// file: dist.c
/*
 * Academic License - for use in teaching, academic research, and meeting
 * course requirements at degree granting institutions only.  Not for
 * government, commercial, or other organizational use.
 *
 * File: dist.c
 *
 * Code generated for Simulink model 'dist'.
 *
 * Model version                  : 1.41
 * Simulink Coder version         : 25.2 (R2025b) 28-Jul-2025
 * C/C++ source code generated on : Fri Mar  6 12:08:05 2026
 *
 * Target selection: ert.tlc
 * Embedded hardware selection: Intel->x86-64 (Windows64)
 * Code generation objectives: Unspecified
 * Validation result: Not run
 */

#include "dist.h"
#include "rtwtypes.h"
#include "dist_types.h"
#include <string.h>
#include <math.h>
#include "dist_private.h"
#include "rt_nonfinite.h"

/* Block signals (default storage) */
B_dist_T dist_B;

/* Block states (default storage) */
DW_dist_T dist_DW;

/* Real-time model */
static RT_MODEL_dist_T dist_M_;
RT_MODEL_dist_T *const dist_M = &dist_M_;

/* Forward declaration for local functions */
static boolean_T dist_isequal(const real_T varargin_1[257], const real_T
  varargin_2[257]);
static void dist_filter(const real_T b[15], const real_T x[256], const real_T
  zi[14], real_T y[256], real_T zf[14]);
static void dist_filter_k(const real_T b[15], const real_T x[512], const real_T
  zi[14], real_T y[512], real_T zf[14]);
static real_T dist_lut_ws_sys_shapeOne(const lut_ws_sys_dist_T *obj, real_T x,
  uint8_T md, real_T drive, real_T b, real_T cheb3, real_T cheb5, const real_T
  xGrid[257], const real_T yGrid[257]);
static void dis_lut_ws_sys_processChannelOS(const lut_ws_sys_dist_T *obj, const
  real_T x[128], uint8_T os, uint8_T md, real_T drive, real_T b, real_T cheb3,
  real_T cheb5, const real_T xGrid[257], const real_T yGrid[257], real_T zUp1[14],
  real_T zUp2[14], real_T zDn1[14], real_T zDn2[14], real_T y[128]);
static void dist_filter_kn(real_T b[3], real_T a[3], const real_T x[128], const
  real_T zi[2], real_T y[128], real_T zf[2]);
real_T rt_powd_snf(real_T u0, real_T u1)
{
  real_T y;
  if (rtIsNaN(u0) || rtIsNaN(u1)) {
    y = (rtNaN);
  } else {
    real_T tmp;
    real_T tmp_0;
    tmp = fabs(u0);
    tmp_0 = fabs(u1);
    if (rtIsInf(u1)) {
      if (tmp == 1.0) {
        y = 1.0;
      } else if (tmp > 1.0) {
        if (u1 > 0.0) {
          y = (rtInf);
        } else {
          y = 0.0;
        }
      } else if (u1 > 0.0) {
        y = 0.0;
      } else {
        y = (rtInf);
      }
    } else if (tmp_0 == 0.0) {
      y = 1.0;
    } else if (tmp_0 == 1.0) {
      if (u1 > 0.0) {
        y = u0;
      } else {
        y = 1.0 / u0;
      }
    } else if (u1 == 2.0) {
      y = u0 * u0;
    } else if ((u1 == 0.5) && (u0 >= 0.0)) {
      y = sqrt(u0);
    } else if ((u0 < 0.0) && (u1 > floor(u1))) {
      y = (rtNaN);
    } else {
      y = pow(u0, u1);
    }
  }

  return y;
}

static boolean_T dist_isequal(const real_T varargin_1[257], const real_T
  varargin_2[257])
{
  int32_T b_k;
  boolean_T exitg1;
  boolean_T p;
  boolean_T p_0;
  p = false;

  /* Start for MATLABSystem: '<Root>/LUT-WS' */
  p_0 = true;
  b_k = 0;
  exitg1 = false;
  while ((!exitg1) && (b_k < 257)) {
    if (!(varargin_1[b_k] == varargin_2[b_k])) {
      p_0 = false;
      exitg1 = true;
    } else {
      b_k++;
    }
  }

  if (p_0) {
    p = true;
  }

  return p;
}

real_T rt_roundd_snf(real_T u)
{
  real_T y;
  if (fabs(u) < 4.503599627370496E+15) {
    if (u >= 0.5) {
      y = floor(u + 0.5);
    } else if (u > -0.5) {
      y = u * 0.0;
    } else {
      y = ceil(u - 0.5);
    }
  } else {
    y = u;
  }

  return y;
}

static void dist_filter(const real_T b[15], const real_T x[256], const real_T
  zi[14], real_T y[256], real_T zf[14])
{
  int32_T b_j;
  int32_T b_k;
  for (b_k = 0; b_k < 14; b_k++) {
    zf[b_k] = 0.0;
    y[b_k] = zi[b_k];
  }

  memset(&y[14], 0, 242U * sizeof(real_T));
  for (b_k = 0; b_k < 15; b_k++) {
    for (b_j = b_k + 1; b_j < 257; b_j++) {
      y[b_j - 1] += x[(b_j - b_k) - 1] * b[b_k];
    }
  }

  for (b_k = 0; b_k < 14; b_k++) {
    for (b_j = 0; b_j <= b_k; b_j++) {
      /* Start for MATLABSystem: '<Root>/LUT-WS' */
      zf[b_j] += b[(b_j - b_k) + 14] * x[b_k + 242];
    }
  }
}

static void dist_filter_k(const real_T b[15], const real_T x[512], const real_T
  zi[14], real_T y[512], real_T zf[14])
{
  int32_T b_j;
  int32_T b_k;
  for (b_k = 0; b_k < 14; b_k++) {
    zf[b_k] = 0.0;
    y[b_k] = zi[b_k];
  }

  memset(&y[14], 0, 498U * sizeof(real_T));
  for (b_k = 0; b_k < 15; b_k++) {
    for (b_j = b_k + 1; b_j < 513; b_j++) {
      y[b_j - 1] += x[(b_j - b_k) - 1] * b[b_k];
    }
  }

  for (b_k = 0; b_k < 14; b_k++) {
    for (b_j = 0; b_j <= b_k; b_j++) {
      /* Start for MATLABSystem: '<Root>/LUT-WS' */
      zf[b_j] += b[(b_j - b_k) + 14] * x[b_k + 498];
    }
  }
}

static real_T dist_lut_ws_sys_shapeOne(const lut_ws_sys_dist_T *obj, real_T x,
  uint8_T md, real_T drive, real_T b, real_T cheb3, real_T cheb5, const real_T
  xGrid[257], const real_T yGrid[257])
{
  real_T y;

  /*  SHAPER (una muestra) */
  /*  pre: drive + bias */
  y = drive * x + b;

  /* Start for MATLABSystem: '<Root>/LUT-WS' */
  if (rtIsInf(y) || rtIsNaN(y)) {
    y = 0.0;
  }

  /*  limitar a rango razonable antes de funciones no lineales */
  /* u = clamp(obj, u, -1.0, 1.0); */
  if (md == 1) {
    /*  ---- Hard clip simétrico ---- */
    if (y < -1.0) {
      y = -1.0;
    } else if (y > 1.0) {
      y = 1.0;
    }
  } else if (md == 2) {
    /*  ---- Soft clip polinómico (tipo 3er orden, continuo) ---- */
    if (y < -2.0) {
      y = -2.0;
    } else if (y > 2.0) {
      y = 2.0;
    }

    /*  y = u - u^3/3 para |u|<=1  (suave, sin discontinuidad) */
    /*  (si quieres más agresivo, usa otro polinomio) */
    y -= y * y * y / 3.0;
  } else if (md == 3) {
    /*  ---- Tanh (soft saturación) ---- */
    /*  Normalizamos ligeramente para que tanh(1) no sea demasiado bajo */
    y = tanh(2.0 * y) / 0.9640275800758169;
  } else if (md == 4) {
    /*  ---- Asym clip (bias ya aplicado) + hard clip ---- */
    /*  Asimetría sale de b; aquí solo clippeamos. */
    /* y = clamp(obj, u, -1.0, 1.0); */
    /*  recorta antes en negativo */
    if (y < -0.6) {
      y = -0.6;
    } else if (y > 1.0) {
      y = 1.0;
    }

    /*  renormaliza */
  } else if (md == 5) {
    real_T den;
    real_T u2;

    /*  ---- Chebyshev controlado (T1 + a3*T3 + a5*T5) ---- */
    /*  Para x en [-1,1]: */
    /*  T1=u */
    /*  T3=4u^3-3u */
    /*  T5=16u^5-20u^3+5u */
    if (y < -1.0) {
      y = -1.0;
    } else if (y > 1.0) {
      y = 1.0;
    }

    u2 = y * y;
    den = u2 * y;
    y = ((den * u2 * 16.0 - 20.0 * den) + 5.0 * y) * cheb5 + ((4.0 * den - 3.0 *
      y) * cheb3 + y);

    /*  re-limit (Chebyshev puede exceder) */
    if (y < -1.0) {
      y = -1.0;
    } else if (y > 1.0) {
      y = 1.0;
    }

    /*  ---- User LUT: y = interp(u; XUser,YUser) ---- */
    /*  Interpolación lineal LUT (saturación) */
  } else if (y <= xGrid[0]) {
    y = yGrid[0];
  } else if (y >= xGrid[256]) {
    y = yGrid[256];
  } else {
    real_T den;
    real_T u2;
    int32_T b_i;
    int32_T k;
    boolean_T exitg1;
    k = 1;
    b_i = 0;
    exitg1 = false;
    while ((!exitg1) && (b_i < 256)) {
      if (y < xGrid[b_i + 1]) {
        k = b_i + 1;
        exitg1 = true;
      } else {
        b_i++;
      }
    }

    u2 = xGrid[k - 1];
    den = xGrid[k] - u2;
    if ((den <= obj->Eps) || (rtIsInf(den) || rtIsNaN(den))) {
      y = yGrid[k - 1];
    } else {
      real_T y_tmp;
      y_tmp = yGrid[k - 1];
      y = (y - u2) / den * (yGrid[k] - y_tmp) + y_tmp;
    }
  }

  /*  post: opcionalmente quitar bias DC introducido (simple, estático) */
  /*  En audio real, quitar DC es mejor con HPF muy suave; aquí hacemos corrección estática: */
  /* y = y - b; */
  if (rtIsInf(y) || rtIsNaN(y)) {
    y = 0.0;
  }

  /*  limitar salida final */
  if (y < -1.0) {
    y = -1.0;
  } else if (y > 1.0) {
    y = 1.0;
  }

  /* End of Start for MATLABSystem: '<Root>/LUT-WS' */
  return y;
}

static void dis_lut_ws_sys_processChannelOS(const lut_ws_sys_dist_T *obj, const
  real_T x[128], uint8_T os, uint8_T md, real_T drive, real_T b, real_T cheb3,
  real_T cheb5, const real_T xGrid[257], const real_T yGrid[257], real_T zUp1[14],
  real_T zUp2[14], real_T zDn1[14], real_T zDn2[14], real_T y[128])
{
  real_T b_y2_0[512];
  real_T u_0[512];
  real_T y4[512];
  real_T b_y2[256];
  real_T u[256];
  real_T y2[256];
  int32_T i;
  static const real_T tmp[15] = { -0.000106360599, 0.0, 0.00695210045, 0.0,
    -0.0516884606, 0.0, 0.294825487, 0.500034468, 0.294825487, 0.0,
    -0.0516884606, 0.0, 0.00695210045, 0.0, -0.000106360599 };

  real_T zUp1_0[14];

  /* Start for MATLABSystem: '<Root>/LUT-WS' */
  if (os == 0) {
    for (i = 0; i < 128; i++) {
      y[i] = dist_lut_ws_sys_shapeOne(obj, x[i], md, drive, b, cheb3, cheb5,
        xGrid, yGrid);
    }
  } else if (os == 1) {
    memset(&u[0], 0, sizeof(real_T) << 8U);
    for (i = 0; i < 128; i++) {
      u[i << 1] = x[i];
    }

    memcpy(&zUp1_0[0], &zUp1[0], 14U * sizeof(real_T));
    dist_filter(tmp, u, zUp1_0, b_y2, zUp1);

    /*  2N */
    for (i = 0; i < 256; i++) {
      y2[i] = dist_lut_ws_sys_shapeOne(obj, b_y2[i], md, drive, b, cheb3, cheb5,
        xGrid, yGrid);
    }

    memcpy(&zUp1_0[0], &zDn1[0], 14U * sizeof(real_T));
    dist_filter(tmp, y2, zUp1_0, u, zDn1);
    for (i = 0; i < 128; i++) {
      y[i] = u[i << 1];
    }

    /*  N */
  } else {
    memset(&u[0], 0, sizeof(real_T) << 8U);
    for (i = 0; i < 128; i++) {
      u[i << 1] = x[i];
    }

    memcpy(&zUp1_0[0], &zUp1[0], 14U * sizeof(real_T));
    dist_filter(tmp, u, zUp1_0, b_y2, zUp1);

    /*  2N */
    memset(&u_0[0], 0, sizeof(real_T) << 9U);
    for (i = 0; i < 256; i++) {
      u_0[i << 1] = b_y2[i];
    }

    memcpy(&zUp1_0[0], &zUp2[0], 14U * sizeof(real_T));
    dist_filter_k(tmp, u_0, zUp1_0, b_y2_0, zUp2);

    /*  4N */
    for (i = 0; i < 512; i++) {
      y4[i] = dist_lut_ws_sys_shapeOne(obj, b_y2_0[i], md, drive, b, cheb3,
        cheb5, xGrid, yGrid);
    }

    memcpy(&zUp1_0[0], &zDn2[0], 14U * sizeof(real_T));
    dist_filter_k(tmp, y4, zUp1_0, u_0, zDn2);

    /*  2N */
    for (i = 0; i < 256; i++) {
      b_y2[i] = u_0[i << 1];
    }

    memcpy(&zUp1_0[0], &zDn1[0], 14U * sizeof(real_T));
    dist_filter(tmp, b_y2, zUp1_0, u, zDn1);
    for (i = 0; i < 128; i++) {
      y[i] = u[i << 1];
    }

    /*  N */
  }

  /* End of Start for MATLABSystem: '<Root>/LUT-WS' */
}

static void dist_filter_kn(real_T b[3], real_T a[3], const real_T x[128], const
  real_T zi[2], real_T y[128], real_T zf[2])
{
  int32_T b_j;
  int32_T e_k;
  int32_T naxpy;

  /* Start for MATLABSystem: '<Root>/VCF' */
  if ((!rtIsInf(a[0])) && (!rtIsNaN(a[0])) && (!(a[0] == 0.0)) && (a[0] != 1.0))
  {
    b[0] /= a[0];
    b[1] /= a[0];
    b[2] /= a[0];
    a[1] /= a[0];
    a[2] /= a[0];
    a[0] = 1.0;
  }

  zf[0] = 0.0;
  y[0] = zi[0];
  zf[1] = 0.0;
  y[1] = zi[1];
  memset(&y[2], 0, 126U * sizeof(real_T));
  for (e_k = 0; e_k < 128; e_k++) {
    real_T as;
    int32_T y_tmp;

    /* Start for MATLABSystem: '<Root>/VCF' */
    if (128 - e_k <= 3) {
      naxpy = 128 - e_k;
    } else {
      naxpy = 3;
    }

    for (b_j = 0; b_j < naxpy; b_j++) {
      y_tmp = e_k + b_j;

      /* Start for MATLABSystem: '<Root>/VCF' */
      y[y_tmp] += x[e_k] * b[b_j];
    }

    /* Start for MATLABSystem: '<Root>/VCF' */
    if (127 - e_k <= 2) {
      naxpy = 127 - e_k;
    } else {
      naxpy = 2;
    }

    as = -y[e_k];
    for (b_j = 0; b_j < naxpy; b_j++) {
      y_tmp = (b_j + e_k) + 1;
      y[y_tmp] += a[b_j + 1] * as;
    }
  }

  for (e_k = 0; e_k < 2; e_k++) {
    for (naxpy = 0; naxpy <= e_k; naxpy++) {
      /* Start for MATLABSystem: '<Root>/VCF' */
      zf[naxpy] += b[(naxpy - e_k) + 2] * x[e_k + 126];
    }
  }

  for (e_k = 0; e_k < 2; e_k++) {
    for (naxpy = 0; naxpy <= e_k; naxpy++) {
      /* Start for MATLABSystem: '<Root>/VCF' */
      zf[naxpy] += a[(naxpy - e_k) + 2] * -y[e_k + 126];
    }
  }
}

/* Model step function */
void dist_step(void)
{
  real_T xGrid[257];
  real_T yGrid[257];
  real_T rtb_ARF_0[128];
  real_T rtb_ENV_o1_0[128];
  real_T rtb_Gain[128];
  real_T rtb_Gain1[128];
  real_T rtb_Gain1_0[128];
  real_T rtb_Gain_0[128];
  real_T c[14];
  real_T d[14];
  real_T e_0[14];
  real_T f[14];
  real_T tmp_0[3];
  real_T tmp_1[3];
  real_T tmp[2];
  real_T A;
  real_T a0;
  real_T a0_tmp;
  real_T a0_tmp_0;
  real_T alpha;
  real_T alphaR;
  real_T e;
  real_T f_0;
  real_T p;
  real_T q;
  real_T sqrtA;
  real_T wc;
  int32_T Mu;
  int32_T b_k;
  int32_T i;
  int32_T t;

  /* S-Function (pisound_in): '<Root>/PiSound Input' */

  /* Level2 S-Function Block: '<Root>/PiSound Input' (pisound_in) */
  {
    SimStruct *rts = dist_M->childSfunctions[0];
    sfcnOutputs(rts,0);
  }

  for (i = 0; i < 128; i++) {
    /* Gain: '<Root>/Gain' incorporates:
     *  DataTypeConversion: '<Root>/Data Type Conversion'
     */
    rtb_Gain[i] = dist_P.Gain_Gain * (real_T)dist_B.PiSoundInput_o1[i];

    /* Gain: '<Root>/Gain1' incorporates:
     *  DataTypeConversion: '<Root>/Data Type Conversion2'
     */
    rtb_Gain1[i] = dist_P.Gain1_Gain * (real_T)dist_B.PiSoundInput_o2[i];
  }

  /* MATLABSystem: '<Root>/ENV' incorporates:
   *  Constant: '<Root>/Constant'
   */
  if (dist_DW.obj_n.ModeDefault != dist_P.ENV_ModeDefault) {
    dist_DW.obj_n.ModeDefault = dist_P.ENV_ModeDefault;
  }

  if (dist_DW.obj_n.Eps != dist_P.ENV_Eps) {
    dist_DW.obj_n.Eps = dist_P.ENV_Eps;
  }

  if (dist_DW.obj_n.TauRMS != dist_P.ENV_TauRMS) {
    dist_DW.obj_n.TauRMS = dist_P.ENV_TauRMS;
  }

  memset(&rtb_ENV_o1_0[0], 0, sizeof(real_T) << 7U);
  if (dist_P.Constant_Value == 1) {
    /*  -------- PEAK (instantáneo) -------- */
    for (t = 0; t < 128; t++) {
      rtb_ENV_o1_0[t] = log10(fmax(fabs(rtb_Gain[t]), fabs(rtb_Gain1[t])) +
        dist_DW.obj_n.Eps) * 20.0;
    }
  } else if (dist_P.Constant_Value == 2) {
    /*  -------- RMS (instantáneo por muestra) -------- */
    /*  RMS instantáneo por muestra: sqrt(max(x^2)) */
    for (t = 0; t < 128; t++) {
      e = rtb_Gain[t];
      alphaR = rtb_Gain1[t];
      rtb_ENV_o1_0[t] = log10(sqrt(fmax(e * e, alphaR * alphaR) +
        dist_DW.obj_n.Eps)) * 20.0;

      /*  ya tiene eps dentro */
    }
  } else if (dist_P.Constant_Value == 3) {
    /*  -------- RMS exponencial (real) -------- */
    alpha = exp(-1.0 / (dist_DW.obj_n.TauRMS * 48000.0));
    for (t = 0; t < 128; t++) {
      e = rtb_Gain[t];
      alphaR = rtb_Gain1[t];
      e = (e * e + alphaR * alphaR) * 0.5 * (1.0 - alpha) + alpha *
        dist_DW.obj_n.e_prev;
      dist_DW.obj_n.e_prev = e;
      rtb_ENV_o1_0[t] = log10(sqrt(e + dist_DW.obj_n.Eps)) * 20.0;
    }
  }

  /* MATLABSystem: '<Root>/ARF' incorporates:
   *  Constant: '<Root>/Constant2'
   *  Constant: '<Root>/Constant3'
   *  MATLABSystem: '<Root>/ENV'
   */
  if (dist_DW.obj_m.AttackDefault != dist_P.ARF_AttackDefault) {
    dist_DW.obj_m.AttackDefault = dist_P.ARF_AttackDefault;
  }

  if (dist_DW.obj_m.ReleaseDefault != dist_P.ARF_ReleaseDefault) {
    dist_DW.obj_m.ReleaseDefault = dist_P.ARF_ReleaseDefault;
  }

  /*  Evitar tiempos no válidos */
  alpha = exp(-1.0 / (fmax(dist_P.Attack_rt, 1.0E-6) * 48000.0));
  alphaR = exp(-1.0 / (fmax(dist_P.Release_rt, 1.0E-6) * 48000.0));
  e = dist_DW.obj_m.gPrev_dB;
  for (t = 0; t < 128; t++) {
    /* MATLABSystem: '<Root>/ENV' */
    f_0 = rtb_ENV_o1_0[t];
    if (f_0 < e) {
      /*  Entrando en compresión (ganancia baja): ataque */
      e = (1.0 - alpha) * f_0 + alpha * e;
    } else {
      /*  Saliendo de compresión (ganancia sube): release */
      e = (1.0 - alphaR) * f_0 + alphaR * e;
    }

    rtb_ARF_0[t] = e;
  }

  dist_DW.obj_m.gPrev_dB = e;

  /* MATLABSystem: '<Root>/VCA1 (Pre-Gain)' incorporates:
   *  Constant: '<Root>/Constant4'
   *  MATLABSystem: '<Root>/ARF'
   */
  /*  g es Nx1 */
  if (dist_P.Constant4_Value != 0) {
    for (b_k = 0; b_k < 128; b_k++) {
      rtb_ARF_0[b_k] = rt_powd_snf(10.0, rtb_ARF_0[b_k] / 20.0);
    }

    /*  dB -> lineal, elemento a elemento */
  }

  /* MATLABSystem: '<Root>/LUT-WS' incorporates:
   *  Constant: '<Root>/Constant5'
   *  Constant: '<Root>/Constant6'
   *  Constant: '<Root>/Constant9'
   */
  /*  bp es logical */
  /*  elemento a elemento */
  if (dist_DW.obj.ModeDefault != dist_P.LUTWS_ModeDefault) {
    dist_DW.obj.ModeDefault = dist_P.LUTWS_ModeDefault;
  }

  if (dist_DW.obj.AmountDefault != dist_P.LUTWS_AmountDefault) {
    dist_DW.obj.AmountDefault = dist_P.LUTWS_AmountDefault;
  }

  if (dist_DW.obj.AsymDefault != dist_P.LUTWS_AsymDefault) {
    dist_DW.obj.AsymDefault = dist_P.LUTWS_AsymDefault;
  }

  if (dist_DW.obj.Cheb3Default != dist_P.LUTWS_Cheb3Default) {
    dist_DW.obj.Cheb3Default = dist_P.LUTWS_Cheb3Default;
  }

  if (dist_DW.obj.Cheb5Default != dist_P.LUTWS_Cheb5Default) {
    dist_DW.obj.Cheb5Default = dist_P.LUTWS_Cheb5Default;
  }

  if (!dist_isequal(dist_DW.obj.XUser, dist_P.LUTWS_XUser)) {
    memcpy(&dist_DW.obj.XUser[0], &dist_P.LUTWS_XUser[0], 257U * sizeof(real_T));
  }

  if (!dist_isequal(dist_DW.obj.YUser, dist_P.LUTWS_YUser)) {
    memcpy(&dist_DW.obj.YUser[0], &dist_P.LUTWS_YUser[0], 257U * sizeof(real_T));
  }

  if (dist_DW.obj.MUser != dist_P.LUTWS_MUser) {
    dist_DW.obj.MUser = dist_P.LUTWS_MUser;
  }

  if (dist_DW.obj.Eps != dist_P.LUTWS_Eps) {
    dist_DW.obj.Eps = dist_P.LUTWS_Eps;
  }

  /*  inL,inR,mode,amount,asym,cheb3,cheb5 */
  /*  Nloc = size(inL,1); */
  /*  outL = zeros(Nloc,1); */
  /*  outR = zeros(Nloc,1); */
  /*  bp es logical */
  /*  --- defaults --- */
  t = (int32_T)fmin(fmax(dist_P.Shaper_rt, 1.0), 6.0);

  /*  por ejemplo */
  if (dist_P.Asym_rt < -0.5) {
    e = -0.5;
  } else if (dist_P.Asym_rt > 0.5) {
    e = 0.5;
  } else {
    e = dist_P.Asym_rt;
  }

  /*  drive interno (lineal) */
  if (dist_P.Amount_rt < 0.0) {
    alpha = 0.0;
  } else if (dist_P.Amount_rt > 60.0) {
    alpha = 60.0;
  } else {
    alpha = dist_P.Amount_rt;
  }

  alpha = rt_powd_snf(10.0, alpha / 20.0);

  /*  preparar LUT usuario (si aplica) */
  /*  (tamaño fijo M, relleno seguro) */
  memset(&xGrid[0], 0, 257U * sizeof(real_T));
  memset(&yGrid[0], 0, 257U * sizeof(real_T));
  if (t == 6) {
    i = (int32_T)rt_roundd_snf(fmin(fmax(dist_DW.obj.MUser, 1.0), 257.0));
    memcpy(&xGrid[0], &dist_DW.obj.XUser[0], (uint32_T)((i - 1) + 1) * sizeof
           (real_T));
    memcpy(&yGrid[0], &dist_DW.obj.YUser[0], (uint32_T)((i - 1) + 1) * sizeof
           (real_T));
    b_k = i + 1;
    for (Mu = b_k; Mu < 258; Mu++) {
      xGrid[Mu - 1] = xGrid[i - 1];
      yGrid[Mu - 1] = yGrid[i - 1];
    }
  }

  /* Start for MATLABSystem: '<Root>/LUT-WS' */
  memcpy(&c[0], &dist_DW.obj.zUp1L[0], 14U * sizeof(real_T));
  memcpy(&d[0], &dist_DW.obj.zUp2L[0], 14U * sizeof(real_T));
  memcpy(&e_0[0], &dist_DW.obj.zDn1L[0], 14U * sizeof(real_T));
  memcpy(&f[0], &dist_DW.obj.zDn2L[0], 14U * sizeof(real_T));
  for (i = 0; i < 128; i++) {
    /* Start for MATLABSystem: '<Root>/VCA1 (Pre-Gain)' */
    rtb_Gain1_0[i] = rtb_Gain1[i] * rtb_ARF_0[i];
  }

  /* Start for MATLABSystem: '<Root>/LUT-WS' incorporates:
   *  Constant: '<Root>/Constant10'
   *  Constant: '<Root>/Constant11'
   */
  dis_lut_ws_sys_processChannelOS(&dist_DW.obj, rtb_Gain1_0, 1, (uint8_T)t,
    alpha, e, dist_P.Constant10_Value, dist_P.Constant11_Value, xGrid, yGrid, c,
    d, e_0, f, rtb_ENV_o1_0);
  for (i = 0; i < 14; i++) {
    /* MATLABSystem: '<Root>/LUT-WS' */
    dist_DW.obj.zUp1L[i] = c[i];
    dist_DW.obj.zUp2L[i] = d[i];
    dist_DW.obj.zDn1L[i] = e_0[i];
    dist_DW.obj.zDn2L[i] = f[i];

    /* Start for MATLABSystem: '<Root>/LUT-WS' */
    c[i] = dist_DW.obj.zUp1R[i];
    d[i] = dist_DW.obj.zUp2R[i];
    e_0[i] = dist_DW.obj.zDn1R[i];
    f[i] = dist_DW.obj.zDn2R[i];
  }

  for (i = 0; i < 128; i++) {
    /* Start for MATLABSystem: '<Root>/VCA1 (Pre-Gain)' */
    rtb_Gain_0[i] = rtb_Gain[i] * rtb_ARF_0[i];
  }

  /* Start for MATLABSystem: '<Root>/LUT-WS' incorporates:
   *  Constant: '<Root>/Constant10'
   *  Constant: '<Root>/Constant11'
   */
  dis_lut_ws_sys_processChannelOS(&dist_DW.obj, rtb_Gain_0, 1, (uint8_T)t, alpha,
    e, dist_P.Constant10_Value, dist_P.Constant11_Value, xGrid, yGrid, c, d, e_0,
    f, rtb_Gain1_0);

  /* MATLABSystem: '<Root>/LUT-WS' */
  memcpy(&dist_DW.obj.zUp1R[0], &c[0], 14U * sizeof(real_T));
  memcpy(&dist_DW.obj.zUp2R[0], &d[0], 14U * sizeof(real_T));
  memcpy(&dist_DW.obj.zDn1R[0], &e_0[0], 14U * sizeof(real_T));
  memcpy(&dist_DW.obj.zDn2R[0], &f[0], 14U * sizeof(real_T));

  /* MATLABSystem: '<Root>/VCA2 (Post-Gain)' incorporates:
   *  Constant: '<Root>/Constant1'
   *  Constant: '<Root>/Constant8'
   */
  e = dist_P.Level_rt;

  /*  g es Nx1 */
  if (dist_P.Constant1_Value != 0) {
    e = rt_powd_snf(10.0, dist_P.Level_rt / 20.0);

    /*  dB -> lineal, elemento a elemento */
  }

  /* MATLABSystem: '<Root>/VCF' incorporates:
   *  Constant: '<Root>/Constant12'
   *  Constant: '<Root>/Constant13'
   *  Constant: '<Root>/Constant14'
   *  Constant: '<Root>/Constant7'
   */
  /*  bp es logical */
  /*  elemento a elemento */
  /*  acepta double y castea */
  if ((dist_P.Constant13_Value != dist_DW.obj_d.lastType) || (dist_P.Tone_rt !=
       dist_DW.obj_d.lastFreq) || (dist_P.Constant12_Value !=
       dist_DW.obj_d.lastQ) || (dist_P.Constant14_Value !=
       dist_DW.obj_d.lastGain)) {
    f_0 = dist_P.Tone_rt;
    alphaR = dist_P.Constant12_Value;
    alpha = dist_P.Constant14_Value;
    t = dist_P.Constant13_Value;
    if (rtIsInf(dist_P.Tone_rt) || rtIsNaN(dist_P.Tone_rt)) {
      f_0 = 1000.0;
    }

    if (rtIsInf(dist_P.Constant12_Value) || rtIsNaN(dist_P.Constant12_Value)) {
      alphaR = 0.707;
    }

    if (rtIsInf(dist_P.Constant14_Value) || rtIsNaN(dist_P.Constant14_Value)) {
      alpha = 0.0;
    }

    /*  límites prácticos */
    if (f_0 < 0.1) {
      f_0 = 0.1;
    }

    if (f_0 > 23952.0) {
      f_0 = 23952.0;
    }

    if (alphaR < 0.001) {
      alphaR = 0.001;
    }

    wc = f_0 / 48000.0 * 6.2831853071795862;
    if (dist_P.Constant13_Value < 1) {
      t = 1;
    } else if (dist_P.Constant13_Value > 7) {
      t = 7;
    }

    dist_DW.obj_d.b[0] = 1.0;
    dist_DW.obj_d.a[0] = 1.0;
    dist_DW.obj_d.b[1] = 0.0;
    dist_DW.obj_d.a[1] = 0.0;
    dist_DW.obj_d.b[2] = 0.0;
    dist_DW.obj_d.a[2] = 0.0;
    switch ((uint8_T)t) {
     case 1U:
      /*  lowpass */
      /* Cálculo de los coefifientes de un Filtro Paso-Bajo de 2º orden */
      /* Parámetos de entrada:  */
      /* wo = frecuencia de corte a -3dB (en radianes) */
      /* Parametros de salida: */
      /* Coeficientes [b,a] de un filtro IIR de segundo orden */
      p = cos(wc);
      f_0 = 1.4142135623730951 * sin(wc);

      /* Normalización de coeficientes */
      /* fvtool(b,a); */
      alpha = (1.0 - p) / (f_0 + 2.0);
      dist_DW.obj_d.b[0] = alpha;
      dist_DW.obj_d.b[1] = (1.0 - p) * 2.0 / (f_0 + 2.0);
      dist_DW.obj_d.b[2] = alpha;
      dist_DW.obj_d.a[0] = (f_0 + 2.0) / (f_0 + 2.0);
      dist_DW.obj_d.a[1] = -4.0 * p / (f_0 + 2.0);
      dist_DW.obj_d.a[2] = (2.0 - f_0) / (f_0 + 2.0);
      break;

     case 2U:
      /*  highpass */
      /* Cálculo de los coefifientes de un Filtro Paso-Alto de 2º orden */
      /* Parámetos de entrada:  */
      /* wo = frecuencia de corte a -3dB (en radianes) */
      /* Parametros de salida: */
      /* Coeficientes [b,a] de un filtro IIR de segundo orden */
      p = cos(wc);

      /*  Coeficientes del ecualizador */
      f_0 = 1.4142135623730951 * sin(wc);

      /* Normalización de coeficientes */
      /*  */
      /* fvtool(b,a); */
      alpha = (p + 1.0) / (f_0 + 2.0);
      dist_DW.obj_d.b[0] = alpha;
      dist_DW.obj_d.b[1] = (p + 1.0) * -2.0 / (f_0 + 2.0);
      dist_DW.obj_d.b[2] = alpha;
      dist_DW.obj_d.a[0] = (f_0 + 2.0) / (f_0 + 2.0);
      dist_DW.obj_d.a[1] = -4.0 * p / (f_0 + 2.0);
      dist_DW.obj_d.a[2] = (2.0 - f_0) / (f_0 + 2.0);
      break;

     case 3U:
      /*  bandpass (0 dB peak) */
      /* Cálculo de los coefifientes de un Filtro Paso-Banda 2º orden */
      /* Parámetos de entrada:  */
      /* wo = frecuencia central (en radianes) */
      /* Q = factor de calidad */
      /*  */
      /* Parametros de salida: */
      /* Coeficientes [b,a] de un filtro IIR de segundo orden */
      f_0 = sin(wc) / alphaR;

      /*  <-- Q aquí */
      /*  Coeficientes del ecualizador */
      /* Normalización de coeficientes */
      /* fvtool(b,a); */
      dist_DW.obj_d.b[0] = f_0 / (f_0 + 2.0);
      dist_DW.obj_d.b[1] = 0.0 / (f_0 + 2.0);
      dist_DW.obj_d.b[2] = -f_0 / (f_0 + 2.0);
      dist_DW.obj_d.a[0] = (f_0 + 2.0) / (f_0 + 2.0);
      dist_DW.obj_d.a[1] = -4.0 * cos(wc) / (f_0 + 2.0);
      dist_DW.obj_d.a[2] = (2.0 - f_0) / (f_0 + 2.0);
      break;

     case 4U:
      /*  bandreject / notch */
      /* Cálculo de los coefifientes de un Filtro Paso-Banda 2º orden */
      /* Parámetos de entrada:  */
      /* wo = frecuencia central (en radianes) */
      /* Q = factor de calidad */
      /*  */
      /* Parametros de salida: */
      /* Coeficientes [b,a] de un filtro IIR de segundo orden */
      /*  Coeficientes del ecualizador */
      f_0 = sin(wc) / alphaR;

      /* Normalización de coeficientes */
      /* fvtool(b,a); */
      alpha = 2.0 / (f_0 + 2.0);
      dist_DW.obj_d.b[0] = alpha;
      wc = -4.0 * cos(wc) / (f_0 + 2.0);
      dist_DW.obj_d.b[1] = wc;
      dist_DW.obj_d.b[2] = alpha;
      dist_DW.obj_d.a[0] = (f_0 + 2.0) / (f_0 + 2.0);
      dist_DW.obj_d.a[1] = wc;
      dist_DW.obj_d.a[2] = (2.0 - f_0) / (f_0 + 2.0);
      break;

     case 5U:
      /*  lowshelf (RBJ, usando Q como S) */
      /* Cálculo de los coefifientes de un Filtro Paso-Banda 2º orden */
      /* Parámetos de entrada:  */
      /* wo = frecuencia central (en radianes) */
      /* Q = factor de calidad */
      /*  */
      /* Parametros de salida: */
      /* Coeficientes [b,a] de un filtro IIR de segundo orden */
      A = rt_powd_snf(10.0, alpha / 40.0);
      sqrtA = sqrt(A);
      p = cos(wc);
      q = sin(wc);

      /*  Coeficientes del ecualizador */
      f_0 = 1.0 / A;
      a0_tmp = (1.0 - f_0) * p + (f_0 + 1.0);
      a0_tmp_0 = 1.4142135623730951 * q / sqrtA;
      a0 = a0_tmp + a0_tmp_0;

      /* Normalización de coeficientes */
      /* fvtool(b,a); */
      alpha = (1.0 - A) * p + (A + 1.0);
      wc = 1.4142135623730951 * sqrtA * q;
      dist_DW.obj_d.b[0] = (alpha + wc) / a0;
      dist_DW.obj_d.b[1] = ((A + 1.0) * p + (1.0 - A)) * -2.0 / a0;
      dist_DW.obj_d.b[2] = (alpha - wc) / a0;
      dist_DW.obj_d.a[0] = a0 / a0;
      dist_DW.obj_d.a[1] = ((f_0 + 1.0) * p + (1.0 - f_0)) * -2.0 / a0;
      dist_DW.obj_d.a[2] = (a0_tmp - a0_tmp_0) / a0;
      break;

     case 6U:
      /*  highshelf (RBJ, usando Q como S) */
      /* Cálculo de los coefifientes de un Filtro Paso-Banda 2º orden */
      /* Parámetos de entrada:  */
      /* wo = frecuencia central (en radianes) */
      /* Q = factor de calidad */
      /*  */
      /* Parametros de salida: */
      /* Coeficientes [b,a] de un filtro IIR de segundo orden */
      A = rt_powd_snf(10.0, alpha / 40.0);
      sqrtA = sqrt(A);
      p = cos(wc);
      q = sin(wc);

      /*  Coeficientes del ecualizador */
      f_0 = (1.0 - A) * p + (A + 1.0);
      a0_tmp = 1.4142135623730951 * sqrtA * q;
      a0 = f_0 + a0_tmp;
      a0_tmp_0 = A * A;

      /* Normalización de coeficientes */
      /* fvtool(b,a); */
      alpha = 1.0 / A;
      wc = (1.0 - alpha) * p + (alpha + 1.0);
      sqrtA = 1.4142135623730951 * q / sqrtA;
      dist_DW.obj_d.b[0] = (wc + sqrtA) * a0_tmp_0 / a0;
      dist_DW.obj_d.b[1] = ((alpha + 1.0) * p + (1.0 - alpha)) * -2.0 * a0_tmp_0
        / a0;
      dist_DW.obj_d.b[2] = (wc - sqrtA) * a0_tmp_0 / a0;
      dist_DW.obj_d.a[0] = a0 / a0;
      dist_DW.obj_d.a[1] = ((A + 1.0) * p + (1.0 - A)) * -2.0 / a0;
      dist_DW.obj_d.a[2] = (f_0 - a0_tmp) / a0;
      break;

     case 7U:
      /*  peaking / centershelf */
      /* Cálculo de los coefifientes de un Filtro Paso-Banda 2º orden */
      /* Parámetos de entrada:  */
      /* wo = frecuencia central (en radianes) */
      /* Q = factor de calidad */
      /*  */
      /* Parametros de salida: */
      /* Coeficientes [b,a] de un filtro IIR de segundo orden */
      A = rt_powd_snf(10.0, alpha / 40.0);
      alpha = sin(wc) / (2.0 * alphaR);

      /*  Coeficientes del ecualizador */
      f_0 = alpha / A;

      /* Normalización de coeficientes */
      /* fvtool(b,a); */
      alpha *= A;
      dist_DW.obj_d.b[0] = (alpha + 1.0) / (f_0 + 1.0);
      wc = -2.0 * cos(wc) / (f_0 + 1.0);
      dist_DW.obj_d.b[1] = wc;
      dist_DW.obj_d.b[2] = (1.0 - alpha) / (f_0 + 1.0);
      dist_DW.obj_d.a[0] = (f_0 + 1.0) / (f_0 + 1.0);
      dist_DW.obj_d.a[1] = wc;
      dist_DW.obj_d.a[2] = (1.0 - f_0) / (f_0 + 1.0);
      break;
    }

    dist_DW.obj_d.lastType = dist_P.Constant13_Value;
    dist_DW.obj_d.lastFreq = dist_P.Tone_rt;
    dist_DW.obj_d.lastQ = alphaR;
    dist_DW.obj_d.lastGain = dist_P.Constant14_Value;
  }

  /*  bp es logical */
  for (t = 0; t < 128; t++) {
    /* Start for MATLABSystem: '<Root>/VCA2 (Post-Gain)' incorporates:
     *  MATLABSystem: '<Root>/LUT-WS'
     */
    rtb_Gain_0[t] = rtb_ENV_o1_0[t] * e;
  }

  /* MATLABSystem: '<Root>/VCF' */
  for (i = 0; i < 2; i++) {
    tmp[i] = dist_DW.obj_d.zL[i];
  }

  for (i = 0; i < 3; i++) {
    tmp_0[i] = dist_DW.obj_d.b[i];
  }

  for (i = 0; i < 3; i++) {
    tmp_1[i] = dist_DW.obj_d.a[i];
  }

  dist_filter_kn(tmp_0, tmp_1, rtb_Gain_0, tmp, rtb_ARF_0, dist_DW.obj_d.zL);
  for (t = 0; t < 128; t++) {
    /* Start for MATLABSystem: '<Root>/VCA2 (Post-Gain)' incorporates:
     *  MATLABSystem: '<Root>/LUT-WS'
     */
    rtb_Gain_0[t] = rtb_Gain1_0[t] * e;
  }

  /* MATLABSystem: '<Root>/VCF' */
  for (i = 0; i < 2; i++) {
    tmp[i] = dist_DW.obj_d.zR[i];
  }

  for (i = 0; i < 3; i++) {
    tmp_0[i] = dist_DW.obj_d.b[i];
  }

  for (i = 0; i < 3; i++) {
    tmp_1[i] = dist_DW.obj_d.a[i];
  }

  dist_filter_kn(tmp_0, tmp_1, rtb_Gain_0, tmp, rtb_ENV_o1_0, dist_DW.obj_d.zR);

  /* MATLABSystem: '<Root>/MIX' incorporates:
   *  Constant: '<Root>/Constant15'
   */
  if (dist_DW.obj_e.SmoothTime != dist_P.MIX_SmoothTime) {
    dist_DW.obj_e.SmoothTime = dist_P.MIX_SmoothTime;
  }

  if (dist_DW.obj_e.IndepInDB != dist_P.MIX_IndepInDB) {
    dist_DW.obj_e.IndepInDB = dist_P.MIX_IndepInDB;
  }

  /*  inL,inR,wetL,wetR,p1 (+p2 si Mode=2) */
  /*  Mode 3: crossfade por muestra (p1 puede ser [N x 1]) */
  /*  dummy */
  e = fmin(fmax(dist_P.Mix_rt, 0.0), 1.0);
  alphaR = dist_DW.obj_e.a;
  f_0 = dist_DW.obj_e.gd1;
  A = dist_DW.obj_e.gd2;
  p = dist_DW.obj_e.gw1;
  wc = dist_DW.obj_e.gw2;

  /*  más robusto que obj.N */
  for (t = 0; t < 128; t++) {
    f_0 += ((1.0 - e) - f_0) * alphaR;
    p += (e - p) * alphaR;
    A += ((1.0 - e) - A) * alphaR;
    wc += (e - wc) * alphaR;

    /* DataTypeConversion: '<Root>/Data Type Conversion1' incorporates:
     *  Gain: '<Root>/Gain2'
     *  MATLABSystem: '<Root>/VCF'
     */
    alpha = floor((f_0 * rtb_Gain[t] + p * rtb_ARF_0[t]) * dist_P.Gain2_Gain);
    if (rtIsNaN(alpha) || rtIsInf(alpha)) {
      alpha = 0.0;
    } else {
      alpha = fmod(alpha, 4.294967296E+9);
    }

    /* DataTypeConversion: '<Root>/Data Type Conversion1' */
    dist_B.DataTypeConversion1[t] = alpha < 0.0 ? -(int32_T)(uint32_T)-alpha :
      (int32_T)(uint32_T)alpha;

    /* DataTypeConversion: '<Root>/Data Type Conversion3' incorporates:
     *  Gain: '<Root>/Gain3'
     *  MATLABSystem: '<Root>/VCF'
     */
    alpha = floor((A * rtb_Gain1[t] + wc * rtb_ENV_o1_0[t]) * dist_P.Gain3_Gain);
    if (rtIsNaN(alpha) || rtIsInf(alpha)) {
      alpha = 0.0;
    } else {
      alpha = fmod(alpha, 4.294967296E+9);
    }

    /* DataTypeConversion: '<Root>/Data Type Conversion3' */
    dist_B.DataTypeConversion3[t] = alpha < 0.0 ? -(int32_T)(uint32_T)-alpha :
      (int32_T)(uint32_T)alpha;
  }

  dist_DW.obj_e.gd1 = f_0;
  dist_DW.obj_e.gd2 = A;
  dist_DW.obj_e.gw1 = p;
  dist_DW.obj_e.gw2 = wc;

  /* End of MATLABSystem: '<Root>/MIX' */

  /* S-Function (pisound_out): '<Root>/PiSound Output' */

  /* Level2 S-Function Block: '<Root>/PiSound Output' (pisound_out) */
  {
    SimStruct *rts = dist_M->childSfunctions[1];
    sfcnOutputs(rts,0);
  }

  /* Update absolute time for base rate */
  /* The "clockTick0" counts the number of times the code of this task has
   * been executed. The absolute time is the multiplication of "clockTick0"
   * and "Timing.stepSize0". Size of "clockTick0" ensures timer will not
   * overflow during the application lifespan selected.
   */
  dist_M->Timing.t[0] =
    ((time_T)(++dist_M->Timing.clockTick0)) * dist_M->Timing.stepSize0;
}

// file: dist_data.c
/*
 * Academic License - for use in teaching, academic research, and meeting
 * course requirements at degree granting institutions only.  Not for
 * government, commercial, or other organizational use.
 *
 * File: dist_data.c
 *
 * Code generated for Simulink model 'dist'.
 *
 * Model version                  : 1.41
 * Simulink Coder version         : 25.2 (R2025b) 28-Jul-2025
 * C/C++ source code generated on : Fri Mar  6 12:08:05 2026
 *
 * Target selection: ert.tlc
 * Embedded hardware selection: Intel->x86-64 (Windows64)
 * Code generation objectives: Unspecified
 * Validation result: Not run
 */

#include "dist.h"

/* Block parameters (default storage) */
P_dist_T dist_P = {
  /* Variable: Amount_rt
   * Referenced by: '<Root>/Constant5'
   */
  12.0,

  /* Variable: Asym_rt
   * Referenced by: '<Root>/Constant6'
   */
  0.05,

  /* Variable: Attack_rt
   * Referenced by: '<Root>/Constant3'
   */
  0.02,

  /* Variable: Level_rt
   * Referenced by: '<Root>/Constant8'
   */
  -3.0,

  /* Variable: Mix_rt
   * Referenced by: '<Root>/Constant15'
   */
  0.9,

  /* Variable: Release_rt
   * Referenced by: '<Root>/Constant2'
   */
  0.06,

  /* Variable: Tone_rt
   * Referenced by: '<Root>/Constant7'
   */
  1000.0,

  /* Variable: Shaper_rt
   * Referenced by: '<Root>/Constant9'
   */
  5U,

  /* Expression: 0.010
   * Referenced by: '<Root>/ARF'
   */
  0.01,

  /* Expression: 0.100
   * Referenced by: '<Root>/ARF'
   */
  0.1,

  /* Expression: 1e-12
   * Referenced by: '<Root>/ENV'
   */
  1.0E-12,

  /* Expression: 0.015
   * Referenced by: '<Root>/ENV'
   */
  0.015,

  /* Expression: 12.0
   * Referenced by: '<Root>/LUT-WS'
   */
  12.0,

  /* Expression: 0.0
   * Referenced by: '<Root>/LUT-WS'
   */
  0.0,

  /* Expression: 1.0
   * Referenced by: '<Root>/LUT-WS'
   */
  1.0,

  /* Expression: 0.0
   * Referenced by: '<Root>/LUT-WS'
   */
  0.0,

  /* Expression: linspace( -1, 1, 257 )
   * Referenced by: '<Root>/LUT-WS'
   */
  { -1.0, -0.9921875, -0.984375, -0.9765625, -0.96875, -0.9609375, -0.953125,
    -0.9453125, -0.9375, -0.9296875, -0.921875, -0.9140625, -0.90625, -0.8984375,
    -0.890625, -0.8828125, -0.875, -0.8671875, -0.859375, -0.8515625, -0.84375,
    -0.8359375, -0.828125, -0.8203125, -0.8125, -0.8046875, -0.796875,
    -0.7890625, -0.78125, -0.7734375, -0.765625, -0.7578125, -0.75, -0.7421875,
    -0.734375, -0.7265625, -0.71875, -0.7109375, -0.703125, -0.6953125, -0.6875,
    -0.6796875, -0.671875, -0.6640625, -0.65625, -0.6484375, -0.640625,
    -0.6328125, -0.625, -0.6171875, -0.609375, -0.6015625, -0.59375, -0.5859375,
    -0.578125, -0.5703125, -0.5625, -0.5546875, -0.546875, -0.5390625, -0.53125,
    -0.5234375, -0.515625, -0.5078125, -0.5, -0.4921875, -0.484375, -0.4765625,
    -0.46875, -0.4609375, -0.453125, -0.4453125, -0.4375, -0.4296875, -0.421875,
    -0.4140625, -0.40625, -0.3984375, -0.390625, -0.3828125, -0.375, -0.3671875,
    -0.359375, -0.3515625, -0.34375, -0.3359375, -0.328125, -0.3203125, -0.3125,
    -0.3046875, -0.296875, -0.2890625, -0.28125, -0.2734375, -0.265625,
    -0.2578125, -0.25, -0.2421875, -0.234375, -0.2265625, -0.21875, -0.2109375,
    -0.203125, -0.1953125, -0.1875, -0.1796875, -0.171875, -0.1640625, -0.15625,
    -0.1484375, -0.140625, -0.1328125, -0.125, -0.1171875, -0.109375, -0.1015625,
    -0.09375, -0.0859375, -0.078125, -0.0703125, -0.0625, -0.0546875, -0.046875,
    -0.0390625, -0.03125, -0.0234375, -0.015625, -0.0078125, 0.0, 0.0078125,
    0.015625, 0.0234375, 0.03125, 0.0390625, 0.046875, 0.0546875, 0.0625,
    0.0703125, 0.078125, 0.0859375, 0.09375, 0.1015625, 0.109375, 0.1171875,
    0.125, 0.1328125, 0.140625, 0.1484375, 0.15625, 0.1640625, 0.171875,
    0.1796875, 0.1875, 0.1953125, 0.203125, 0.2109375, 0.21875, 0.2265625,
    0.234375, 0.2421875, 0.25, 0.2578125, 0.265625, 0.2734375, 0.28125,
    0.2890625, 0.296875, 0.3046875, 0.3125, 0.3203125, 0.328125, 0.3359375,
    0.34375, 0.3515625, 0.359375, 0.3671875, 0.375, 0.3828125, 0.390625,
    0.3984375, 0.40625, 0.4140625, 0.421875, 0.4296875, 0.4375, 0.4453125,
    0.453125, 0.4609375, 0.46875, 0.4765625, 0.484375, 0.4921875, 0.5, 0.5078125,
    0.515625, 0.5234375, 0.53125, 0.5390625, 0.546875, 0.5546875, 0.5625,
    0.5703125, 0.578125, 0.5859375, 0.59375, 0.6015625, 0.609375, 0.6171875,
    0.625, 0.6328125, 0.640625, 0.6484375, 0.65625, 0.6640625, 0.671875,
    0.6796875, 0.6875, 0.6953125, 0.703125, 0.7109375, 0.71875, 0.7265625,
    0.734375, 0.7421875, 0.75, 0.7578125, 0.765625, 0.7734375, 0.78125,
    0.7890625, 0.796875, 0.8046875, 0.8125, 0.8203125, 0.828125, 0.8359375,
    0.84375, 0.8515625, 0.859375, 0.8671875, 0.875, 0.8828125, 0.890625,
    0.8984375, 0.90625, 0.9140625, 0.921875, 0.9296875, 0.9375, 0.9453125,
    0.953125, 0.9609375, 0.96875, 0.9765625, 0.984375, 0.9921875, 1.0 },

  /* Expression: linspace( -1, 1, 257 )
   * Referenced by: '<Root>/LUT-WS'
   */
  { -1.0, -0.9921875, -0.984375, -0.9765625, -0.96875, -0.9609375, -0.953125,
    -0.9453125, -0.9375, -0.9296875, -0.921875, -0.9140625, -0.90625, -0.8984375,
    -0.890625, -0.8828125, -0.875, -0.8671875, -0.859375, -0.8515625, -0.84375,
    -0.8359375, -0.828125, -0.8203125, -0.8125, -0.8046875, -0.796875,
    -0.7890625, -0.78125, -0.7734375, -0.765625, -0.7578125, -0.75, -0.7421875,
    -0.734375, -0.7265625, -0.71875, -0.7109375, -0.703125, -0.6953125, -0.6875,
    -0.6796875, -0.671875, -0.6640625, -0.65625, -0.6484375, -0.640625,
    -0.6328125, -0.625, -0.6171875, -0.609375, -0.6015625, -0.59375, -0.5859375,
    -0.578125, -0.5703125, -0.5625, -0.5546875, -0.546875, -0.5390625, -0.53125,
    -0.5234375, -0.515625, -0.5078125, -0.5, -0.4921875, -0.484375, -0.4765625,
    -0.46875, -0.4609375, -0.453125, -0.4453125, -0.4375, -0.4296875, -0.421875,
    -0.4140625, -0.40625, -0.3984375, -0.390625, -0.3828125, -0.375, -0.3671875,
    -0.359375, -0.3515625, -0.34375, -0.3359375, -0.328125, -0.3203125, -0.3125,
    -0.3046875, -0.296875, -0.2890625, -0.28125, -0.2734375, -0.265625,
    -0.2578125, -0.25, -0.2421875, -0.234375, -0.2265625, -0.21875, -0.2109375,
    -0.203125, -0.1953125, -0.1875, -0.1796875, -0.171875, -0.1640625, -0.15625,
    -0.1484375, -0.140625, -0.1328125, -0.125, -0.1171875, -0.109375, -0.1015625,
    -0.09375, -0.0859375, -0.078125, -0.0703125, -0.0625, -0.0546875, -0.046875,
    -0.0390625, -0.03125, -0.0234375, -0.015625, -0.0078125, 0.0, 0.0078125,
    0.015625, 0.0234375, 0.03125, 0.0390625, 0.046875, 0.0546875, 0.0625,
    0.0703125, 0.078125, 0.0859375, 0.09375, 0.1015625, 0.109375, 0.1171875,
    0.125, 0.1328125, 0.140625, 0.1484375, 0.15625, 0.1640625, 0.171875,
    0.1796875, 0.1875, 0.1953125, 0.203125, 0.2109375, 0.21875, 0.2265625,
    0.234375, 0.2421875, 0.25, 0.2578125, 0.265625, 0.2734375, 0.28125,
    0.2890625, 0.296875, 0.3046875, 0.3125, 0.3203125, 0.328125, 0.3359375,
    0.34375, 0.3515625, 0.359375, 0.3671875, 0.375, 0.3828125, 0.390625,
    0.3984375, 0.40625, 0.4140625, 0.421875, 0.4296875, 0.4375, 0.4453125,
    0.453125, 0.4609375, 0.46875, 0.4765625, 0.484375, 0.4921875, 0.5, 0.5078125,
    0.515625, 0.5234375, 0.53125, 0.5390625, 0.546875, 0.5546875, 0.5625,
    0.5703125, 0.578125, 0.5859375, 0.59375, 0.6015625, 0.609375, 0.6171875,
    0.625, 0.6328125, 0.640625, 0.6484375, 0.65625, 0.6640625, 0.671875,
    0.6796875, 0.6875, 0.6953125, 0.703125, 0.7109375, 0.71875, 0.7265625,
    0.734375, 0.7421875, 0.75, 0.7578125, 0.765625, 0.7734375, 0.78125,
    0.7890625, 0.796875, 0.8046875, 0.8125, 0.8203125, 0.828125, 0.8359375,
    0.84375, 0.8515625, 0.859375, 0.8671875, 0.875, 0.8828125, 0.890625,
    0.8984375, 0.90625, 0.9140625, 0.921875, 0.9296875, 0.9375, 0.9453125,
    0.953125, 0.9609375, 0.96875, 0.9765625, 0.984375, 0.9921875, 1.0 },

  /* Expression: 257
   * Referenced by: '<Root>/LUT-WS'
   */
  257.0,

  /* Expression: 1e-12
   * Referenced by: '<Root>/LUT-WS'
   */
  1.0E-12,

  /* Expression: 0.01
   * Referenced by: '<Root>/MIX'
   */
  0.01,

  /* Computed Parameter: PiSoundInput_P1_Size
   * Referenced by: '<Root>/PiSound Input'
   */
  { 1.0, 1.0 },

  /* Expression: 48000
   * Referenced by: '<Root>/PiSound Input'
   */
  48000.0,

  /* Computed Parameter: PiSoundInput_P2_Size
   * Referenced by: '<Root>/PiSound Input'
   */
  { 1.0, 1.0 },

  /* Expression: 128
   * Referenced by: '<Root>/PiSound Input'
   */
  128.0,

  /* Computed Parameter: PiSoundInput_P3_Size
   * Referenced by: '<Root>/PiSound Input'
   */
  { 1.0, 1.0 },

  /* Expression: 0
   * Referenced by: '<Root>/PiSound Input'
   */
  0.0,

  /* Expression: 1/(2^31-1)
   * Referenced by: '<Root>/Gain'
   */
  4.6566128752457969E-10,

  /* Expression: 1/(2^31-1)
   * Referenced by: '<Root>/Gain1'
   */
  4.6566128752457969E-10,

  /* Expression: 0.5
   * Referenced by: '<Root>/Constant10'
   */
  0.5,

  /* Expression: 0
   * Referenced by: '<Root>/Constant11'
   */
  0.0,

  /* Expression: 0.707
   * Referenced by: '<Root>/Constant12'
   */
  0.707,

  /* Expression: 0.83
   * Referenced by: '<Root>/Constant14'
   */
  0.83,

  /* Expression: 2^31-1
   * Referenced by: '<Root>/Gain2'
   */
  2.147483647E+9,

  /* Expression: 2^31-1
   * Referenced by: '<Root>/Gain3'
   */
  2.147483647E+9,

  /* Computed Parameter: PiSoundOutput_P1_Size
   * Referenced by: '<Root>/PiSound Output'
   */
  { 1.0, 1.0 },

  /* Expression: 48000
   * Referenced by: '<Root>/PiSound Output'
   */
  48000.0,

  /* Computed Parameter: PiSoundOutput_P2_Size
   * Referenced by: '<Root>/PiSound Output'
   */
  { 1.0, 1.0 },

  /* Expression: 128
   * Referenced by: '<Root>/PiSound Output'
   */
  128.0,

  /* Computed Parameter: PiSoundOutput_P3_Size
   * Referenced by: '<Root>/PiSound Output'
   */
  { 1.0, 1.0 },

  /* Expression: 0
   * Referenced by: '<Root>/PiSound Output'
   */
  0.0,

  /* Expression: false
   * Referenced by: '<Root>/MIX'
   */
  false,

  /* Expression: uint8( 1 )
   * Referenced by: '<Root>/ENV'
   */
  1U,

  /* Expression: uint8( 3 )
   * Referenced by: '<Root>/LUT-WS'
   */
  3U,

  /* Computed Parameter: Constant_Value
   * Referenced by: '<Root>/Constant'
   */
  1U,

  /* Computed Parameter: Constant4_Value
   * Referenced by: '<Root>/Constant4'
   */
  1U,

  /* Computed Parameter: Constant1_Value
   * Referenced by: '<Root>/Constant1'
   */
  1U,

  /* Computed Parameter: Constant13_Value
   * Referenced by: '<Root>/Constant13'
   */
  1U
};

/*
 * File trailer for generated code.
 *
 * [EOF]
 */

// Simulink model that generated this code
simulink model "dist"  (R2025b)
settings: Solver=FixedStepDiscrete  StartTime=0.0  StopTime=inf  FixedStep=128/48000  RelTol=1e-3
model workspace (MATLAB code in the model file):
  | Gain_rt = Simulink.Parameter(1.0);
  | Bypass_rt = Simulink.Parameter(false);
undefined symbols (not defined in the file): Amount_rt, Asym_rt, Attack_rt, Level_rt, Mix_rt, Release_rt, Shaper_rt, Tone_rt

== system dist ==
  ARF : MATLABSystem  System=arf_sys  N=128  Fs=48000  AttackDefault=0.010  ReleaseDefault=0.100  SimulateUsing=Code generation
  Constant{,1,4,13} (4 alike) : Constant  OutDataTypeStr=uint8
  Constant10 : Constant  Value=0.5  OutDataTypeStr=double
  Constant11 : Constant  Value=0  OutDataTypeStr=double
  Constant12 : Constant  Value=0.707  OutDataTypeStr=double
  Constant14 : Constant  Value=0.83  OutDataTypeStr=double
  Constant15 : Constant  Value=Mix_rt  OutDataTypeStr=double
  Constant2 : Constant  Value=Release_rt  OutDataTypeStr=double
  Constant3 : Constant  Value=Attack_rt  OutDataTypeStr=double
  Constant5 : Constant  Value=Amount_rt  OutDataTypeStr=double
  Constant6 : Constant  Value=Asym_rt  OutDataTypeStr=double
  Constant7 : Constant  Value=Tone_rt  OutDataTypeStr=double
  Constant8 : Constant  Value=Level_rt  OutDataTypeStr=double
  Constant9 : Constant  Value=Shaper_rt  OutDataTypeStr=uint8
  Data Type Conversion : DataTypeConversion  OutDataTypeStr=double  SaturateOnIntegerOverflow=off  RndMeth=Floor
  Data Type Conversion1 : DataTypeConversion  OutDataTypeStr=int32  SaturateOnIntegerOverflow=off  RndMeth=Floor
  Data Type Conversion2 : DataTypeConversion  OutDataTypeStr=double  SaturateOnIntegerOverflow=off  RndMeth=Floor
  Data Type Conversion3 : DataTypeConversion  OutDataTypeStr=int32  SaturateOnIntegerOverflow=off  RndMeth=Floor
  ENV : MATLABSystem  System=env_sys  N=128  Fs=48000  ModeDefault=uint8( 1 )  Eps=1e-12  TauRMS=0.015  SimulateUsing=Code generation
  Gain : Gain  Gain=1/(2^31-1)
  Gain1 : Gain  Gain=1/(2^31-1)
  Gain2 : Gain  Gain=2^31-1
  Gain3 : Gain  Gain=2^31-1
  LUT-WS : MATLABSystem  System=lut_ws_sys  N=128  M=257  bypass=uint8(0)  OS=uint8(1)  HB15=[ -1.06360599e-04, 0, 6.95210045e-03, 0, -5.16884606e-02, 0, 2.94825487e-01, 5.00034468e-01, 2.94825487e-01, 0, -5.16884606e-02, 0, 6.95210045e-03, 0, -1.06360599e-04 ]  ModeDefault=uint8( 3 )  AmountDefault=12.0  AsymDefault=0.0  Cheb3Default=1.0  Cheb5Default=0.0  XUser=linspace( -1, 1, 257 )  YUser=linspace( -1, 1, 257 )  MUser=257  Eps=1e-12  SimulateUsing=Code generation
  MIX : MATLABSystem  System=mix_sys  N=128  Fs=48000  Mode=uint8( 0 )  SmoothTime=0.01  IndepInDB=false  SimulateUsing=Code generation
  PiSound Input : S-Function  FunctionName=pisound_in  Parameters=48000, 128, 0  SFunctionDeploymentMode=off  EnableBusSupport=off
  PiSound Output : S-Function  FunctionName=pisound_out  Parameters=48000, 128, 0  SFunctionDeploymentMode=off  EnableBusSupport=off
  VCA1 (Pre-Gain) : MATLABSystem  System=vca_sys  N=128  Fs=48000  bypass=uint8(0)  SimulateUsing=Code generation
  VCA2 (Post-Gain) : MATLABSystem  System=vca_sys  N=128  Fs=48000  bypass=uint8(0)  SimulateUsing=Code generation
  VCF : MATLABSystem  System=vcf_sys  N=128  Fs=48000  bypass=uint8(0)  SimulateUsing=Code generation
  wires:
  PiSound Input/1 -> Data Type Conversion/1
  PiSound Input/2 -> Data Type Conversion2/1
  Data Type Conversion1/1 -> PiSound Output/1
  Data Type Conversion3/1 -> PiSound Output/2
  Gain2/1 -> Data Type Conversion1/1
  Gain3/1 -> Data Type Conversion3/1
  Data Type Conversion/1 -> Gain/1
  Data Type Conversion2/1 -> Gain1/1
  Gain/1 -> ENV/1, MIX/1, VCA1 (Pre-Gain)/2
  Gain1/1 -> MIX/2, ENV/2, VCA1 (Pre-Gain)/1
  Constant/1 -> ENV/3
  Constant1/1 -> VCA2 (Post-Gain)/4
  Constant2/1 -> ARF/3
  Constant3/1 -> ARF/2
  ARF/1 -> VCA1 (Pre-Gain)/3
  VCA1 (Pre-Gain)/1 -> LUT-WS/1
  VCA1 (Pre-Gain)/2 -> LUT-WS/2
  LUT-WS/1 -> VCA2 (Post-Gain)/1
  LUT-WS/2 -> VCA2 (Post-Gain)/2
  Constant8/1 -> VCA2 (Post-Gain)/3
  Constant9/1 -> LUT-WS/3
  Constant5/1 -> LUT-WS/4
  Constant6/1 -> LUT-WS/5
  Constant7/1 -> VCF/4
  VCA2 (Post-Gain)/1 -> VCF/1
  VCA2 (Post-Gain)/2 -> VCF/2
  ENV/1 -> ARF/1
  Constant4/1 -> VCA1 (Pre-Gain)/4
  Constant10/1 -> LUT-WS/6
  Constant11/1 -> LUT-WS/7
  Constant12/1 -> VCF/5
  Constant13/1 -> VCF/3
  Constant14/1 -> VCF/6
  MIX/1 -> Gain2/1
  MIX/2 -> Gain3/1
  VCF/1 -> MIX/3
  VCF/2 -> MIX/4
  Constant15/1 -> MIX/5
